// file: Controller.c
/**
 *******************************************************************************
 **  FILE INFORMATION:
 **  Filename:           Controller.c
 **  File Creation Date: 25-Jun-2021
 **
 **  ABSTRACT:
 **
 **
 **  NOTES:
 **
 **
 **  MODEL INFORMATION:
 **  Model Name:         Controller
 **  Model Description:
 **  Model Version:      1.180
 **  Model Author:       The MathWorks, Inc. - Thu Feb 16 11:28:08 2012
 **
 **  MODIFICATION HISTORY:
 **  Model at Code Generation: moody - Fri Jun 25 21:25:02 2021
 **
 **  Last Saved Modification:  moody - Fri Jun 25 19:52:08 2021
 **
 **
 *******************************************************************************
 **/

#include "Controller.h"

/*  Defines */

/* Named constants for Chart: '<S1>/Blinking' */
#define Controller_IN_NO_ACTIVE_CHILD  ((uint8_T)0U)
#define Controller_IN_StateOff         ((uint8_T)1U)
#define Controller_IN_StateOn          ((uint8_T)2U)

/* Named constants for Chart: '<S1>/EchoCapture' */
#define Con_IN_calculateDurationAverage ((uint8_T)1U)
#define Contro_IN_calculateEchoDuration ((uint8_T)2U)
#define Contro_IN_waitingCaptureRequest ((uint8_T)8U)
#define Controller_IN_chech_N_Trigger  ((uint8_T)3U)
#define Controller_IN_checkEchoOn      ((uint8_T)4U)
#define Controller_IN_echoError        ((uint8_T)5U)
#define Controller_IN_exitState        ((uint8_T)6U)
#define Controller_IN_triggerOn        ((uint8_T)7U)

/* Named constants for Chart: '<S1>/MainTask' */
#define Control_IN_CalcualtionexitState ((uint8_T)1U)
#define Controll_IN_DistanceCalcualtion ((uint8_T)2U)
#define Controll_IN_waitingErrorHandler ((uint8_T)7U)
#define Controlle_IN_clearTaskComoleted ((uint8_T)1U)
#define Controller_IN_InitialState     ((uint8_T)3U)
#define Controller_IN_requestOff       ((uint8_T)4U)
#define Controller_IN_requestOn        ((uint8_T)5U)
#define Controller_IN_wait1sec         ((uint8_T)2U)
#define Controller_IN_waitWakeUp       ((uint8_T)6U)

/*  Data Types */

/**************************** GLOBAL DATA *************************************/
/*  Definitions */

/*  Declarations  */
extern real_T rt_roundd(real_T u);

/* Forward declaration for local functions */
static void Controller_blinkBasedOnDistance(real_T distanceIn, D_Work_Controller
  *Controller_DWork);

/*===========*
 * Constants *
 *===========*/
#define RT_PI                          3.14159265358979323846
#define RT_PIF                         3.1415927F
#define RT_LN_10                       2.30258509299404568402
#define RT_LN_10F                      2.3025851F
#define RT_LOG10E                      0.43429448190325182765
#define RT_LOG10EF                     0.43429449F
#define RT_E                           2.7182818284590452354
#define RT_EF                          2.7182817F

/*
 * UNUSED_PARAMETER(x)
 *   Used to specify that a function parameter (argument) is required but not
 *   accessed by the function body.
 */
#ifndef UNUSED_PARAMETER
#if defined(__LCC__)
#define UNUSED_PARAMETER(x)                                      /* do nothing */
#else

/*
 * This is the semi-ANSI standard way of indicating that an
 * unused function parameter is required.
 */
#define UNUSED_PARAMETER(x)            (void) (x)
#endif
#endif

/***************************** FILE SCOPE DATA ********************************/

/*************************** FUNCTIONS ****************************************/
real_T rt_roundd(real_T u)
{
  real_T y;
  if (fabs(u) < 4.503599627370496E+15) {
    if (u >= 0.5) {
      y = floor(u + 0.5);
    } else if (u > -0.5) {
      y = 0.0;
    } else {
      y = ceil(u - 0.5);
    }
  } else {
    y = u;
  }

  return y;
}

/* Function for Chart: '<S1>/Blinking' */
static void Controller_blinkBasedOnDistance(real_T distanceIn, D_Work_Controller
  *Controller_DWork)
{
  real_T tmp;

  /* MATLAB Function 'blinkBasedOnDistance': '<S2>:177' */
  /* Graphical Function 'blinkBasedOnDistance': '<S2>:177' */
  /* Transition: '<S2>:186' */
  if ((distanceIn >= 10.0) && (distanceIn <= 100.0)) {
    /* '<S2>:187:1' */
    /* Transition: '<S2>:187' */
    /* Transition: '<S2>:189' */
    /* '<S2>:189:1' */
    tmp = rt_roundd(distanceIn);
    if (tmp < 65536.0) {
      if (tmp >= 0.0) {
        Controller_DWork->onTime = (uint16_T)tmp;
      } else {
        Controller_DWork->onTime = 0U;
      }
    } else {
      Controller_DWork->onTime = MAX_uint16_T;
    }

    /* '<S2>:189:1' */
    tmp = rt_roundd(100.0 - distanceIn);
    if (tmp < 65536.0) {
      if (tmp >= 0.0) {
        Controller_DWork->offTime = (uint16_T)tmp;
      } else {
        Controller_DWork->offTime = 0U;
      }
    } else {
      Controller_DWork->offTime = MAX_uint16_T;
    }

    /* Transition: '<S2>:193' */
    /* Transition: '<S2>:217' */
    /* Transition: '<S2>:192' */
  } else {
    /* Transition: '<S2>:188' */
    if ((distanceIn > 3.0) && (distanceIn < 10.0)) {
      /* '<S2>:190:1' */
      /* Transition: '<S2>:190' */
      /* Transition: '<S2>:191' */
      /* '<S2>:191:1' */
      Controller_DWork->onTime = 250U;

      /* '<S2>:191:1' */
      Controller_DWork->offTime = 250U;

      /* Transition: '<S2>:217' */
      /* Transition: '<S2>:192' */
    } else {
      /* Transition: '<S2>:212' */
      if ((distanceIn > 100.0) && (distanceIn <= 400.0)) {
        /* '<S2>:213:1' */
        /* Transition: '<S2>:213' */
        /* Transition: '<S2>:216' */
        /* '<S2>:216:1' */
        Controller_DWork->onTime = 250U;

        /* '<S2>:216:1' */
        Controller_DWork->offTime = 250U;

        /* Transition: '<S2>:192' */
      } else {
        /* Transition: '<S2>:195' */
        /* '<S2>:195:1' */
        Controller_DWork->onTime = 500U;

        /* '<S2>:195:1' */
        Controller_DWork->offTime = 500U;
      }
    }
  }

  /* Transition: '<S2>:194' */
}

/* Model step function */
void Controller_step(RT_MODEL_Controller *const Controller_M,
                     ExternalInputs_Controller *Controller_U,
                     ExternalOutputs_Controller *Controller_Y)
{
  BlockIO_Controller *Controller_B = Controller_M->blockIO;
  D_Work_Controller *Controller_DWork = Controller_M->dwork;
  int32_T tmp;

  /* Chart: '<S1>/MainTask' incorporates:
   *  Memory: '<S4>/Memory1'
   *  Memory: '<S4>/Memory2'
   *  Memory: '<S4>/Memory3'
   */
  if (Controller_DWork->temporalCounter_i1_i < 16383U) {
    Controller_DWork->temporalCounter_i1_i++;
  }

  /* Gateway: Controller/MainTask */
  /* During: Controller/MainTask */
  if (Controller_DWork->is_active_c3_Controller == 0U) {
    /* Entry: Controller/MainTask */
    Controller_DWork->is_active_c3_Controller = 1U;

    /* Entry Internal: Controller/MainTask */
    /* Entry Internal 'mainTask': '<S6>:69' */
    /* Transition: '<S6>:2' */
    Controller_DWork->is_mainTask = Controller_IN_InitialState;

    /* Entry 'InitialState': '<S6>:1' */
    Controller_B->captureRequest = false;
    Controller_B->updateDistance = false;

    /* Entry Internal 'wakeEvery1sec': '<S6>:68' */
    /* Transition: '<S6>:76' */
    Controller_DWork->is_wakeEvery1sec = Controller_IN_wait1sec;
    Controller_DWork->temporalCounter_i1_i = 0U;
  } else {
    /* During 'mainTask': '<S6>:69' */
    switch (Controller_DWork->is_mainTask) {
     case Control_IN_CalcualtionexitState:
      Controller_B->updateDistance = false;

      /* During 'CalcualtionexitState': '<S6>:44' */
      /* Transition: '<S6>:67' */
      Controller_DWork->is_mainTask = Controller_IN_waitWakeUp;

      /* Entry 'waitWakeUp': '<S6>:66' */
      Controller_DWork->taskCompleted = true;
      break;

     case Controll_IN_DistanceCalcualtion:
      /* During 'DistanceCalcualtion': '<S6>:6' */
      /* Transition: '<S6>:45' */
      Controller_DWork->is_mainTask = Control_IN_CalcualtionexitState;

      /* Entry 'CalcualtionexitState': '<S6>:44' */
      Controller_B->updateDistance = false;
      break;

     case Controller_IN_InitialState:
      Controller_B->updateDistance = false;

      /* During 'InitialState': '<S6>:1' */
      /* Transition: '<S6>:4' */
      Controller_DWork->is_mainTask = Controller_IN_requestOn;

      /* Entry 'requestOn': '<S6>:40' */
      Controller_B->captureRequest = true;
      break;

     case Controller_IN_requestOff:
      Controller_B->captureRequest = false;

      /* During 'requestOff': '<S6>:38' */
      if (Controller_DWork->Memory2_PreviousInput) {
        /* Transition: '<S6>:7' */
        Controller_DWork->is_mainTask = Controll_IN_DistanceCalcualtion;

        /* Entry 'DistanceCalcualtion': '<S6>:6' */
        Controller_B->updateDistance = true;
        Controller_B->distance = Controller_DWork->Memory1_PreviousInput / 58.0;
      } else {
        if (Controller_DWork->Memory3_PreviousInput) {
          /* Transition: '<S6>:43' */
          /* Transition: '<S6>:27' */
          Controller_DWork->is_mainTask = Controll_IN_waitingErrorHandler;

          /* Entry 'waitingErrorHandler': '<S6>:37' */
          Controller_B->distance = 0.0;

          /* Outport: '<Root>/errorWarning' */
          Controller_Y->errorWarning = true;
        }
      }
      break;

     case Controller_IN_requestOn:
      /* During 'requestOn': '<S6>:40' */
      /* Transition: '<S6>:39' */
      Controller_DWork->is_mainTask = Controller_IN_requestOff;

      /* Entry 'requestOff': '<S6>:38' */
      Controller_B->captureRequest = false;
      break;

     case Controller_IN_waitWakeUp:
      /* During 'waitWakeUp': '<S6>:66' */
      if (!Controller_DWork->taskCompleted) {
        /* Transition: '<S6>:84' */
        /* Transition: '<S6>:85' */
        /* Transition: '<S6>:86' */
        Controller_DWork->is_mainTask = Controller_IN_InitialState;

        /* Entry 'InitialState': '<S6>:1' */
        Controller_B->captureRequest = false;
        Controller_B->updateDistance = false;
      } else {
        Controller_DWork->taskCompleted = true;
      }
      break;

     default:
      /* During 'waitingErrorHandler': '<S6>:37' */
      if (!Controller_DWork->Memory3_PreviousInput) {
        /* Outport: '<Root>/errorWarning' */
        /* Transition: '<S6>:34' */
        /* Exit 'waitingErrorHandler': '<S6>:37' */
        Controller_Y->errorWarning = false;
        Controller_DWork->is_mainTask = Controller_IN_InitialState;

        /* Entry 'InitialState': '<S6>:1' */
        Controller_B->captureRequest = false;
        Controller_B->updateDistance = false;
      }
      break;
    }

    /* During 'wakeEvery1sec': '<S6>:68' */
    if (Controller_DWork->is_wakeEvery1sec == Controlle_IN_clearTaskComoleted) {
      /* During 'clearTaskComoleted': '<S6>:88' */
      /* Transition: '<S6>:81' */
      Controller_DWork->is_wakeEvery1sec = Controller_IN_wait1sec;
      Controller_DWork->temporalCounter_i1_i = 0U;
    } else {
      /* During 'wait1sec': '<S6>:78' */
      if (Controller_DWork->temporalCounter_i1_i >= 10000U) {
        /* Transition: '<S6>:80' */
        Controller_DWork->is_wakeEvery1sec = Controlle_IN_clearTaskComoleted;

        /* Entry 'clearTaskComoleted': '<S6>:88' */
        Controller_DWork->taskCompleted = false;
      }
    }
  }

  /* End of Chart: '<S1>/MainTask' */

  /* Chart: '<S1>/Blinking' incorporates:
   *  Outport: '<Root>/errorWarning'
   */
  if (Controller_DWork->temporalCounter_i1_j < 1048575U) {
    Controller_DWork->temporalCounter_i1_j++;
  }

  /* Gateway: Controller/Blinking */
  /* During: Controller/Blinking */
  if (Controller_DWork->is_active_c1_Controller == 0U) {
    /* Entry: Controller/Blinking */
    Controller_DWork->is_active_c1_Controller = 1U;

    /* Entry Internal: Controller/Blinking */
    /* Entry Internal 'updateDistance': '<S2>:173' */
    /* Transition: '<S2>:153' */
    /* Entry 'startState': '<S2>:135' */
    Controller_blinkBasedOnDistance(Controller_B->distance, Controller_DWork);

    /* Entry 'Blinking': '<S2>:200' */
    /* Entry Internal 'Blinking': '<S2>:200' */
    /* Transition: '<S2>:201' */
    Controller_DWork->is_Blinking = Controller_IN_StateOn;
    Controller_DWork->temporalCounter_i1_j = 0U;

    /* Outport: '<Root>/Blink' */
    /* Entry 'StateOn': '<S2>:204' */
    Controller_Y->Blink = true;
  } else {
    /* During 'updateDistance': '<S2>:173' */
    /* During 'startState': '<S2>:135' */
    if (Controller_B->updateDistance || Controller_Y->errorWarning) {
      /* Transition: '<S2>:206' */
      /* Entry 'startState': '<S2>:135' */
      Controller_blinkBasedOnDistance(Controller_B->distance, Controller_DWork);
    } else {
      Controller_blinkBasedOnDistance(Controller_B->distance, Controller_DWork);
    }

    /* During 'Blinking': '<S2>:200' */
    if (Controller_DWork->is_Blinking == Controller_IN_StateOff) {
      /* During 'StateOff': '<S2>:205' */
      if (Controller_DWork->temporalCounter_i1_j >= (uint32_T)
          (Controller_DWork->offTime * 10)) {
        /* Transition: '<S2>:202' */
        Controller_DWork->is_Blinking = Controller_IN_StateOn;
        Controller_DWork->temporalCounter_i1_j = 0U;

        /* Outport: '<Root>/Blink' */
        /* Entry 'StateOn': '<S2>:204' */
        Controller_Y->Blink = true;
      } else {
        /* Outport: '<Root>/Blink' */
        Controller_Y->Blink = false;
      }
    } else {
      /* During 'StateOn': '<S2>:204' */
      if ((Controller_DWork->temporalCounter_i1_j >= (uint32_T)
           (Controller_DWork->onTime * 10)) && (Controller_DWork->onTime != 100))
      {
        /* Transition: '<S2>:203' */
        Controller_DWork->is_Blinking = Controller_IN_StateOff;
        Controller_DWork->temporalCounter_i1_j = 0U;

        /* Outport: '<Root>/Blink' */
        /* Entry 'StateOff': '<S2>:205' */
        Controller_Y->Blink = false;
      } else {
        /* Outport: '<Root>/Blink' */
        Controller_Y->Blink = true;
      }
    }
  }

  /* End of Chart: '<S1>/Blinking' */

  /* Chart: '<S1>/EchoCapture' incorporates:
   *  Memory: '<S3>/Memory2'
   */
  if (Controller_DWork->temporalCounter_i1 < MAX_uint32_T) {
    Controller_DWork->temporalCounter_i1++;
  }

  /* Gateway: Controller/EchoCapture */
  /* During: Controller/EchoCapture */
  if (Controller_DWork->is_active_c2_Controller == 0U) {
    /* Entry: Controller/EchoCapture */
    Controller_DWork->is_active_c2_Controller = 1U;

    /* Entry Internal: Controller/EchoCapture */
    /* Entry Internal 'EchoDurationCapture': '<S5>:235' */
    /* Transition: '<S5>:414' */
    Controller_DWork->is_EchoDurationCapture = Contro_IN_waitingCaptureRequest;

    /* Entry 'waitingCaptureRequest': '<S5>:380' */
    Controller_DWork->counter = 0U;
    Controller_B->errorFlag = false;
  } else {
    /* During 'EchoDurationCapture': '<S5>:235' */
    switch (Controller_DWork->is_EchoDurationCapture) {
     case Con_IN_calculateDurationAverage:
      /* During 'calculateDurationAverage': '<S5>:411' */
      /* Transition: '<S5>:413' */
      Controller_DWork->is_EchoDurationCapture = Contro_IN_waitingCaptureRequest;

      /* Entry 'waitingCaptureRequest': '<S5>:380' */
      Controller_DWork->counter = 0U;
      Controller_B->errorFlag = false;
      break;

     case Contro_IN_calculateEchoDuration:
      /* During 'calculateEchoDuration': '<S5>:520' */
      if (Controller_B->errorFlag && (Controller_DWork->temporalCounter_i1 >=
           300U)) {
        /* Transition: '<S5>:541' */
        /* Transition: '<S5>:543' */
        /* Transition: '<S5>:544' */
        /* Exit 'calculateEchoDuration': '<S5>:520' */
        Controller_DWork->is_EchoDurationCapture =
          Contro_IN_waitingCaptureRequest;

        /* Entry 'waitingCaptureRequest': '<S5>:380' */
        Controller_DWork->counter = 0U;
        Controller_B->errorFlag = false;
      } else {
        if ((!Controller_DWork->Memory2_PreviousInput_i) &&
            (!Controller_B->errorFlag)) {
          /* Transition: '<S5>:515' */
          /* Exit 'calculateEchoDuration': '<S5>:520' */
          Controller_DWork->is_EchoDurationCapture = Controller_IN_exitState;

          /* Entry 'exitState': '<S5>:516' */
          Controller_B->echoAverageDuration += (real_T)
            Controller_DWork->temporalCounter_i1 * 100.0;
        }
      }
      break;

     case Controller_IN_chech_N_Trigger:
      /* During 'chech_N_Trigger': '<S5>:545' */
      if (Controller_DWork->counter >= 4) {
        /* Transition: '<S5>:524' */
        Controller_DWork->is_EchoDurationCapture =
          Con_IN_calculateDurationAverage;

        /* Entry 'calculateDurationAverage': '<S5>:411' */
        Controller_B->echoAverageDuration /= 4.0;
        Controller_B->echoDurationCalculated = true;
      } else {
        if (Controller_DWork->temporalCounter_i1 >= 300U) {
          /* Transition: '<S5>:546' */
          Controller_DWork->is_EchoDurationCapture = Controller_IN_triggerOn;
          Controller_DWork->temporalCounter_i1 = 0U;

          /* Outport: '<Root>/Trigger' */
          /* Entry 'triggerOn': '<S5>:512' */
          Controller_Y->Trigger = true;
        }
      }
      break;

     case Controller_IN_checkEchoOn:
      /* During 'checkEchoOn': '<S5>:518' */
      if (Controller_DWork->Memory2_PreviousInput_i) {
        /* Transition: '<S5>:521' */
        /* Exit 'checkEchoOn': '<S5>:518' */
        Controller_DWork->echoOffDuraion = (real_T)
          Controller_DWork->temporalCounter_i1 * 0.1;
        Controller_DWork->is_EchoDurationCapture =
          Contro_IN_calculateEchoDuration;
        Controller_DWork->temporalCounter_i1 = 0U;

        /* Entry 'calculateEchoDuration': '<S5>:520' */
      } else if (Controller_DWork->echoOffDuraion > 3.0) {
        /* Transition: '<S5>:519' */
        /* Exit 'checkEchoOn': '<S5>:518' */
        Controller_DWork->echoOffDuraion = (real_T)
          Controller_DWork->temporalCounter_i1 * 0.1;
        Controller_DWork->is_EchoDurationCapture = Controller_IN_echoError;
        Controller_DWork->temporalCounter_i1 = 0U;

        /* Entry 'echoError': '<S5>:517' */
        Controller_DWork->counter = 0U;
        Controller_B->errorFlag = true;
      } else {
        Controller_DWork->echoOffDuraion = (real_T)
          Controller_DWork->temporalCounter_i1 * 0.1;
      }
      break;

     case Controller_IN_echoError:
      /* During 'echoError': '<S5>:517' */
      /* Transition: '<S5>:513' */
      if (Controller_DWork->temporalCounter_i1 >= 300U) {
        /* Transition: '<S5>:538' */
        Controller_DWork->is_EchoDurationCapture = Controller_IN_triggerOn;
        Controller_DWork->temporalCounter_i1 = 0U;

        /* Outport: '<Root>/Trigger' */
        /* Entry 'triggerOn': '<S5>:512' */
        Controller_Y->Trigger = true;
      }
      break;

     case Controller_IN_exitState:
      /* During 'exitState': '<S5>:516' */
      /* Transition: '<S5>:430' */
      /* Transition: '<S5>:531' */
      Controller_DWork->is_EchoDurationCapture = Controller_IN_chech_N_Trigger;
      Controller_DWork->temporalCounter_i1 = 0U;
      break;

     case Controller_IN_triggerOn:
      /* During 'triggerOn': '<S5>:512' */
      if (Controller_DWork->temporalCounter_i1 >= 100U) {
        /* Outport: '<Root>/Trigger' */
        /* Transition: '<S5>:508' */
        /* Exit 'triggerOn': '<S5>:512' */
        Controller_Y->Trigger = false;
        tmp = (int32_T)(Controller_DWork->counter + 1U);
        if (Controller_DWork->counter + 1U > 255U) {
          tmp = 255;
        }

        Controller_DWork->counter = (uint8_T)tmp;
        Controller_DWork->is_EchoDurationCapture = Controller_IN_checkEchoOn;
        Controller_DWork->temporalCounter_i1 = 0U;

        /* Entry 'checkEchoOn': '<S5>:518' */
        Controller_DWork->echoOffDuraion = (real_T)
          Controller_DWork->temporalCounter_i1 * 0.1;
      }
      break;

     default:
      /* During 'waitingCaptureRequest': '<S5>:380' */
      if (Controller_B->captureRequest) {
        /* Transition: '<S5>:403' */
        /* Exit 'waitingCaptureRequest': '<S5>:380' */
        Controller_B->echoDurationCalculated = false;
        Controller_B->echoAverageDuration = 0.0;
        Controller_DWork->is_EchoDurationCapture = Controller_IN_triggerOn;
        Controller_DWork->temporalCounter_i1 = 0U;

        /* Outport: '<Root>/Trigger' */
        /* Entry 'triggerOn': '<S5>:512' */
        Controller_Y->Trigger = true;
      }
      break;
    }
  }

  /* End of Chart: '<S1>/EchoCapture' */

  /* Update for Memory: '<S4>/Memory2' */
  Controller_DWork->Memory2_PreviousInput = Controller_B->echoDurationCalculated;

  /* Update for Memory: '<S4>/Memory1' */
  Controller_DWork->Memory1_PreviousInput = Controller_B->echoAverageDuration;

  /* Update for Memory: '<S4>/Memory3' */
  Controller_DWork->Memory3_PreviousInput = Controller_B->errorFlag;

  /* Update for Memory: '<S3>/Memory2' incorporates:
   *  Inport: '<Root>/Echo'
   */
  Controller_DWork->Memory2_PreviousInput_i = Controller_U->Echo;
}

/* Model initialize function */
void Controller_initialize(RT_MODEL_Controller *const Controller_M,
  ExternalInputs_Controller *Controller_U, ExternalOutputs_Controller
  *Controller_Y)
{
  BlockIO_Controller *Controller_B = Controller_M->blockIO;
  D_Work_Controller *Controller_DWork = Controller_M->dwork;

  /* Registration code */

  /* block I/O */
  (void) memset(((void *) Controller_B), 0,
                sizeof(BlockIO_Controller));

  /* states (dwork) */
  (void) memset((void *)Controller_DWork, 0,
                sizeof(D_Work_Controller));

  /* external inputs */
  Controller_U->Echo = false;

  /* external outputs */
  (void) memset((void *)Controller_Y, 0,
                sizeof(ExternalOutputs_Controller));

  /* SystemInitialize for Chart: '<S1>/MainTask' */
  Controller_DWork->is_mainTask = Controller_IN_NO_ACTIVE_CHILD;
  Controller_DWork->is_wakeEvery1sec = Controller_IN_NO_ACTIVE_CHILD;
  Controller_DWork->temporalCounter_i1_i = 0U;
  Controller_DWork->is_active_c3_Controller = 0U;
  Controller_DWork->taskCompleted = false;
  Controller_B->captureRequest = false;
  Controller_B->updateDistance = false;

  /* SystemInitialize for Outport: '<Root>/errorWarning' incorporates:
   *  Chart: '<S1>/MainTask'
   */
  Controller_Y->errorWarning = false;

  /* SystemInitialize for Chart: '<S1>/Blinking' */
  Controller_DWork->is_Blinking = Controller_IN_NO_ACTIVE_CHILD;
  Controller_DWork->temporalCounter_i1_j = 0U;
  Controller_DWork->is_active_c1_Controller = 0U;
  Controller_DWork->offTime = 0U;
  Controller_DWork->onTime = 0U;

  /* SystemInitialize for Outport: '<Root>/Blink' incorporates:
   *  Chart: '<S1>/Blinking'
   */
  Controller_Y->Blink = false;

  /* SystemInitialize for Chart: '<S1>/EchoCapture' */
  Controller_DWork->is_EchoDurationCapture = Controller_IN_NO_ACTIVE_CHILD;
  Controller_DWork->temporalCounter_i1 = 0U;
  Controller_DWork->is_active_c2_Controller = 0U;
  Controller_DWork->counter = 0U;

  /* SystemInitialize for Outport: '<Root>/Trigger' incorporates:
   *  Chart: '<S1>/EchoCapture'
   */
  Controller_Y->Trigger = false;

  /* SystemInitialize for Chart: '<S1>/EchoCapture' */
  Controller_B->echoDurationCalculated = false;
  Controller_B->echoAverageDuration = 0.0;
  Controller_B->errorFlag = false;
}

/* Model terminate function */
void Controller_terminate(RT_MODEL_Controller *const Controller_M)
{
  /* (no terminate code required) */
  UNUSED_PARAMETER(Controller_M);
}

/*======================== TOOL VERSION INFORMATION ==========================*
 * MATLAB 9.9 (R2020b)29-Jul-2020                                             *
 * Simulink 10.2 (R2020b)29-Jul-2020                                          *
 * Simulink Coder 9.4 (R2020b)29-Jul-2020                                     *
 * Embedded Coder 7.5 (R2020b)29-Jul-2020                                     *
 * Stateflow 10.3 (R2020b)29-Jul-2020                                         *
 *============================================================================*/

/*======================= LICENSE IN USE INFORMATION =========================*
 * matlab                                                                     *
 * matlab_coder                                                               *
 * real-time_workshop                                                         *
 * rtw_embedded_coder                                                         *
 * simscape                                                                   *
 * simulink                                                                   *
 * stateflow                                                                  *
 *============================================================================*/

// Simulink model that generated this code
simulink model "Controller"  (R2020b)
settings: Solver=FixedStepDiscrete  StartTime=0.0  StopTime=20  FixedStep=1e-4  RelTol=1e-3

== system Controller ==
  note: Level Estimator Project - MBSD
  Echo : Inport  OutDataTypeStr=boolean  PortDimensions=1
  Controller : Subsystem
  Blink : Outport
  Trigger : Outport  Port=2  OutDataTypeStr=boolean  PortDimensions=1
  errorWarning : Outport  Port=3
  wires:
  Controller/1(levelBlinkOut) -> Blink/1
  Controller/3(Trigger) -> Trigger/1
  Controller/2(errorWarning) -> errorWarning/1
  Echo/1 -> Controller/1(Echo)

== system Controller/Controller ==
  Echo : Inport
  Blinking : Stateflow chart  TreatAsAtomicUnit=on
  DRCon2 : Subsystem
  DRConv1 : Subsystem
  EchoCapture : Stateflow chart  TreatAsAtomicUnit=on
  MainTask : Stateflow chart  TreatAsAtomicUnit=on
  levelBlinkOut : Outport
  errorWarning : Outport  Port=2
  Trigger : Outport  Port=3
  wires:
  MainTask/4(errorWarning) -> errorWarning/1, Blinking/3(errorWarning)
  DRConv1/1(Trigger) -> MainTask/1(echoDurationCalculated)
  DRConv1/2(Trigger1) -> MainTask/2(echoDuration)
  DRCon2/1(Trigger) -> EchoCapture/1(EchoInput)
  EchoCapture/2(echoDurationCalculated) -> DRConv1/1(echoDuraionA)
  EchoCapture/3(echoAverageDuration) -> DRConv1/2(echoDuraionA1)
  MainTask/1(captureRequest) -> EchoCapture/2(captureRequest)
  EchoCapture/1(Trigger) -> Trigger/1
  EchoCapture/4(errorFlag) -> DRConv1/3(echoDuraionA2)
  DRConv1/3(Trigger2) -> MainTask/3(errorFlag)
  Blinking/1(levelBlinkOut) -> levelBlinkOut/1
  Echo/1 -> DRCon2/1(In1)
  MainTask/2(distance) -> Blinking/1(distance)
  MainTask/3(updateDistance) -> Blinking/2(newDistanceFlag)

== system Controller/Controller/DRCon2 ==
  In1 : Inport
  Memory2 : Memory
  Rate Transition2 : RateTransition
  Trigger : Outport
  wires:
  Rate Transition2/1 -> Trigger/1
  In1/1 -> Memory2/1
  Memory2/1 -> Rate Transition2/1

== system Controller/Controller/DRConv1 ==
  echoDuraionA : Inport
  echoDuraionA1 : Inport  Port=2
  echoDuraionA2 : Inport  Port=3
  Memory1 : Memory
  Memory2 : Memory
  Memory3 : Memory
  Rate Transition1 : RateTransition
  Rate Transition2 : RateTransition
  Rate Transition3 : RateTransition
  Trigger : Outport
  Trigger1 : Outport  Port=2
  Trigger2 : Outport  Port=3
  wires:
  Rate Transition2/1 -> Trigger/1
  echoDuraionA/1 -> Memory2/1
  Memory2/1 -> Rate Transition2/1
  Rate Transition1/1 -> Trigger1/1
  echoDuraionA1/1 -> Memory1/1
  Memory1/1 -> Rate Transition1/1
  Rate Transition3/1 -> Trigger2/1
  echoDuraionA2/1 -> Memory3/1
  Memory3/1 -> Rate Transition3/1

== stateflow chart Controller/Blinking ==
  settings: initializeOutput=1
  state Blinking [parallel]
    settings: executionOrder=2
    state StateOn
      levelBlinkOut = true;
    state StateOff
      levelBlinkOut = false;
    (default) -> StateOn
    StateOff -> StateOn : after(offTime,msec)
    StateOn -> StateOff : [after(onTime,msec)...
        |  && onTime ~= 100]
  state updateDistance [parallel]
    settings: executionOrder=1
    state startState
      blinkBasedOnDistance(distance)
    state blinkBasedOnDistance(distanceIn) [function]
      (default) -> (junction 178) : % decide blinkTaskIndex based on distance
      (junction 178) -> (junction 179) [order 1] : [ distanceIn >= 10 && distanceIn <= 100 ]
      (junction 178) -> (junction 180) [order 2]
      (junction 179) -> (junction 184) : {onTime = uint16(distanceIn); offTime = uint16(100-distanceIn);}
      (junction 180) -> (junction 181) [order 1] : [distanceIn > 3 && distanceIn < 10]
      (junction 180) -> (junction 211) [order 2]
      (junction 181) -> (junction 183) : {onTime = 250; offTime = 250;}
      (junction 211) -> (junction 214) [order 1] : [distanceIn >  100 &&  distanceIn <= 400]
      (junction 211) -> (junction 182) [order 2] : {onTime = 500; offTime = 500;}
      (junction 214) -> (junction 215) : {onTime = 250; offTime = 250;}
      (junction 215) -> (junction 182)
      (junction 183) -> (junction 215)
      (junction 184) -> (junction 183)
      (junction 182) -> (junction 185)
    (default) -> startState
    startState -> startState : [newDistanceFlag == true || errorWarning == true]
  data: distanceIn function_input; distance input double size=1; levelBlinkOut output boolean size=1 =false; newDistanceFlag input boolean size=1 =false; errorWarning input boolean size=1; offTime local uint16 size=1 =uint16(0); onTime local uint16 size=1 =uint16(0)

== stateflow chart Controller/EchoCapture ==
  state EchoDurationCapture [parallel]
    settings: executionOrder=1
    state waitingCaptureRequest
      entry:
      counter = 0;
      errorFlag = false;
      exit:
      echoDurationCalculated = false;
      echoAverageDuration = 0;
    state calculateDurationAverage
      entry:
      echoAverageDuration = ...
      echoAverageDuration/4;
      echoDurationCalculated = true;
    state triggerOn
      entry:
      Trigger = true;
      exit:
      Trigger = false
      counter = counter+1;
    state chech_N_Trigger
    state echoError
      entry:
      counter = 0;
      errorFlag =  true;
    state checkEchoOn
      entry, during, exit:
      echoOffDuraion = elapsed(msec);
    state calculateEchoDuration
      entry, during, exit:
      echoOnDuraion = elapsed(usec);
    state exitState
      entry:
      echoAverageDuration = ...
      echoAverageDuration + echoOnDuraion;
    (default) -> waitingCaptureRequest
    (junction 542) -> waitingCaptureRequest
    calculateDurationAverage -> waitingCaptureRequest
    (junction 540) -> (junction 542) : after(30, msec)
    waitingCaptureRequest -> triggerOn : [captureRequest == true]
    chech_N_Trigger -> calculateDurationAverage [order 1] : [counter >= 4]
    (junction 537) -> triggerOn : after(30, msec)
    echoError -> (junction 537)
    chech_N_Trigger -> triggerOn [order 2] : after(30, msec)
    triggerOn -> checkEchoOn : after(10, msec)
    (junction 429) -> chech_N_Trigger
    checkEchoOn -> echoError [order 2] : [echoOffDuraion > 3]
    checkEchoOn -> calculateEchoDuration [order 1] : [EchoInput == true]
    calculateEchoDuration -> (junction 540) [order 1] : [errorFlag ==  true]
    calculateEchoDuration -> exitState [order 2] : [EchoInput == false &&  errorFlag == false]
    exitState -> (junction 429)
  data: Trigger output boolean =false; EchoInput input; counter local uint8 =uint8(0); captureRequest input boolean size=1; echoDurationCalculated output boolean size=1 =false; echoAverageDuration output double size=1 =0; errorFlag output boolean size=1 =false; echoOffDuraion local; echoOnDuraion local

== stateflow chart Controller/MainTask ==
  state mainTask [parallel]
    settings: executionOrder=1
    state InitialState
      entry:
      captureRequest = false;
      updateDistance = false;
    state waitingErrorHandler
      entry:
      distance = 0;
      errorWarning = true;
      exit:
      errorWarning = false;
    state requestOn
      entry:
      captureRequest = true;
    state requestOff
      entry:
      captureRequest = false;
    state DistanceCalcualtion
      entry:
      updateDistance = true;
      distance = echoDuration/58;
    state CalcualtionexitState
      entry:
      updateDistance = false;
    state waitWakeUp
      taskCompleted = true
    (default) -> InitialState
    waitingErrorHandler -> InitialState : [errorFlag == false]
    (junction 83) -> InitialState
    (junction 82) -> (junction 83)
    InitialState -> requestOn
    (junction 42) -> waitingErrorHandler
    requestOn -> requestOff
    requestOff -> (junction 42) [order 2] : [errorFlag == true]
    requestOff -> DistanceCalcualtion [order 1] : [echoDurationCalculated == true]
    DistanceCalcualtion -> CalcualtionexitState
    CalcualtionexitState -> waitWakeUp
    waitWakeUp -> (junction 82) : [taskCompleted == false]
  state wakeEvery1sec [parallel]
    settings: executionOrder=2
    state wait1sec
    state clearTaskComoleted
      taskCompleted = false
    (default) -> wait1sec
    clearTaskComoleted -> wait1sec
    wait1sec -> clearTaskComoleted : after(1000, msec)
  data: captureRequest output boolean size=1 =false; echoDurationCalculated input boolean size=1; distance output double size=1; updateDistance output boolean size=1 =false; echoDuration input double size=1; errorFlag input boolean size=1; errorWarning output boolean size=1 =false; taskCompleted local boolean size=1 =false
